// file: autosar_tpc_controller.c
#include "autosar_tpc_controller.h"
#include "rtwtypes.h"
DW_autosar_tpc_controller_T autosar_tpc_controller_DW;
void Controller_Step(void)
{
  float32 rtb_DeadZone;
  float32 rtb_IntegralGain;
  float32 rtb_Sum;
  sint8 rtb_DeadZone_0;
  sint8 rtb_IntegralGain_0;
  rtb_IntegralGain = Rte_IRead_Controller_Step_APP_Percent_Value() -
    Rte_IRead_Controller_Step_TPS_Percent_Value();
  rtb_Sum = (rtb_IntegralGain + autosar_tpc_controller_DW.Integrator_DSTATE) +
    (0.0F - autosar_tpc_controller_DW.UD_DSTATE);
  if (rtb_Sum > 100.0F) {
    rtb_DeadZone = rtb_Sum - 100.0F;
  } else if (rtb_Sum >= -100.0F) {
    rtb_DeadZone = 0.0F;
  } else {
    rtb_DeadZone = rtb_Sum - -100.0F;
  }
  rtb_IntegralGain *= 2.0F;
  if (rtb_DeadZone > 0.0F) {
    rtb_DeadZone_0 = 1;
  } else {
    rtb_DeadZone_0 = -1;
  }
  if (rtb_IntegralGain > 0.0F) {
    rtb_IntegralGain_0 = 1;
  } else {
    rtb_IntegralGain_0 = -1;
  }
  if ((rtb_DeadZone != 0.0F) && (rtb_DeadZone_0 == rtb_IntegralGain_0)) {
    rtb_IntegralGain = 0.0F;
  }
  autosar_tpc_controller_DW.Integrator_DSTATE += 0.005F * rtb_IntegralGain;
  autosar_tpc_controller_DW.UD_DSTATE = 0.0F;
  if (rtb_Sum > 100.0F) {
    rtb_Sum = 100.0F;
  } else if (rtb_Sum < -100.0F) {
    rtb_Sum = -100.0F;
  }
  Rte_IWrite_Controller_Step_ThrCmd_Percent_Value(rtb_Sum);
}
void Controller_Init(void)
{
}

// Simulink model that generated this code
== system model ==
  Inport#1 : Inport
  Inport#2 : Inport
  Outport#1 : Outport  <- 1: PIDController#1
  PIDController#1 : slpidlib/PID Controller  Controller=PID  Form=Parallel  TimeDomain=Discrete-time  IntegratorMethod=Forward Euler  P=1  I=2  D=0  N=100  InitialConditionForIntegrator=0  ExternalReset=none  LimitOutput=on  UpperSaturationLimit=100  LowerSaturationLimit=-100  <- 1: Sum#1
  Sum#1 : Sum  Inputs=+-  <- 1: Inport#1, 2: Inport#2
